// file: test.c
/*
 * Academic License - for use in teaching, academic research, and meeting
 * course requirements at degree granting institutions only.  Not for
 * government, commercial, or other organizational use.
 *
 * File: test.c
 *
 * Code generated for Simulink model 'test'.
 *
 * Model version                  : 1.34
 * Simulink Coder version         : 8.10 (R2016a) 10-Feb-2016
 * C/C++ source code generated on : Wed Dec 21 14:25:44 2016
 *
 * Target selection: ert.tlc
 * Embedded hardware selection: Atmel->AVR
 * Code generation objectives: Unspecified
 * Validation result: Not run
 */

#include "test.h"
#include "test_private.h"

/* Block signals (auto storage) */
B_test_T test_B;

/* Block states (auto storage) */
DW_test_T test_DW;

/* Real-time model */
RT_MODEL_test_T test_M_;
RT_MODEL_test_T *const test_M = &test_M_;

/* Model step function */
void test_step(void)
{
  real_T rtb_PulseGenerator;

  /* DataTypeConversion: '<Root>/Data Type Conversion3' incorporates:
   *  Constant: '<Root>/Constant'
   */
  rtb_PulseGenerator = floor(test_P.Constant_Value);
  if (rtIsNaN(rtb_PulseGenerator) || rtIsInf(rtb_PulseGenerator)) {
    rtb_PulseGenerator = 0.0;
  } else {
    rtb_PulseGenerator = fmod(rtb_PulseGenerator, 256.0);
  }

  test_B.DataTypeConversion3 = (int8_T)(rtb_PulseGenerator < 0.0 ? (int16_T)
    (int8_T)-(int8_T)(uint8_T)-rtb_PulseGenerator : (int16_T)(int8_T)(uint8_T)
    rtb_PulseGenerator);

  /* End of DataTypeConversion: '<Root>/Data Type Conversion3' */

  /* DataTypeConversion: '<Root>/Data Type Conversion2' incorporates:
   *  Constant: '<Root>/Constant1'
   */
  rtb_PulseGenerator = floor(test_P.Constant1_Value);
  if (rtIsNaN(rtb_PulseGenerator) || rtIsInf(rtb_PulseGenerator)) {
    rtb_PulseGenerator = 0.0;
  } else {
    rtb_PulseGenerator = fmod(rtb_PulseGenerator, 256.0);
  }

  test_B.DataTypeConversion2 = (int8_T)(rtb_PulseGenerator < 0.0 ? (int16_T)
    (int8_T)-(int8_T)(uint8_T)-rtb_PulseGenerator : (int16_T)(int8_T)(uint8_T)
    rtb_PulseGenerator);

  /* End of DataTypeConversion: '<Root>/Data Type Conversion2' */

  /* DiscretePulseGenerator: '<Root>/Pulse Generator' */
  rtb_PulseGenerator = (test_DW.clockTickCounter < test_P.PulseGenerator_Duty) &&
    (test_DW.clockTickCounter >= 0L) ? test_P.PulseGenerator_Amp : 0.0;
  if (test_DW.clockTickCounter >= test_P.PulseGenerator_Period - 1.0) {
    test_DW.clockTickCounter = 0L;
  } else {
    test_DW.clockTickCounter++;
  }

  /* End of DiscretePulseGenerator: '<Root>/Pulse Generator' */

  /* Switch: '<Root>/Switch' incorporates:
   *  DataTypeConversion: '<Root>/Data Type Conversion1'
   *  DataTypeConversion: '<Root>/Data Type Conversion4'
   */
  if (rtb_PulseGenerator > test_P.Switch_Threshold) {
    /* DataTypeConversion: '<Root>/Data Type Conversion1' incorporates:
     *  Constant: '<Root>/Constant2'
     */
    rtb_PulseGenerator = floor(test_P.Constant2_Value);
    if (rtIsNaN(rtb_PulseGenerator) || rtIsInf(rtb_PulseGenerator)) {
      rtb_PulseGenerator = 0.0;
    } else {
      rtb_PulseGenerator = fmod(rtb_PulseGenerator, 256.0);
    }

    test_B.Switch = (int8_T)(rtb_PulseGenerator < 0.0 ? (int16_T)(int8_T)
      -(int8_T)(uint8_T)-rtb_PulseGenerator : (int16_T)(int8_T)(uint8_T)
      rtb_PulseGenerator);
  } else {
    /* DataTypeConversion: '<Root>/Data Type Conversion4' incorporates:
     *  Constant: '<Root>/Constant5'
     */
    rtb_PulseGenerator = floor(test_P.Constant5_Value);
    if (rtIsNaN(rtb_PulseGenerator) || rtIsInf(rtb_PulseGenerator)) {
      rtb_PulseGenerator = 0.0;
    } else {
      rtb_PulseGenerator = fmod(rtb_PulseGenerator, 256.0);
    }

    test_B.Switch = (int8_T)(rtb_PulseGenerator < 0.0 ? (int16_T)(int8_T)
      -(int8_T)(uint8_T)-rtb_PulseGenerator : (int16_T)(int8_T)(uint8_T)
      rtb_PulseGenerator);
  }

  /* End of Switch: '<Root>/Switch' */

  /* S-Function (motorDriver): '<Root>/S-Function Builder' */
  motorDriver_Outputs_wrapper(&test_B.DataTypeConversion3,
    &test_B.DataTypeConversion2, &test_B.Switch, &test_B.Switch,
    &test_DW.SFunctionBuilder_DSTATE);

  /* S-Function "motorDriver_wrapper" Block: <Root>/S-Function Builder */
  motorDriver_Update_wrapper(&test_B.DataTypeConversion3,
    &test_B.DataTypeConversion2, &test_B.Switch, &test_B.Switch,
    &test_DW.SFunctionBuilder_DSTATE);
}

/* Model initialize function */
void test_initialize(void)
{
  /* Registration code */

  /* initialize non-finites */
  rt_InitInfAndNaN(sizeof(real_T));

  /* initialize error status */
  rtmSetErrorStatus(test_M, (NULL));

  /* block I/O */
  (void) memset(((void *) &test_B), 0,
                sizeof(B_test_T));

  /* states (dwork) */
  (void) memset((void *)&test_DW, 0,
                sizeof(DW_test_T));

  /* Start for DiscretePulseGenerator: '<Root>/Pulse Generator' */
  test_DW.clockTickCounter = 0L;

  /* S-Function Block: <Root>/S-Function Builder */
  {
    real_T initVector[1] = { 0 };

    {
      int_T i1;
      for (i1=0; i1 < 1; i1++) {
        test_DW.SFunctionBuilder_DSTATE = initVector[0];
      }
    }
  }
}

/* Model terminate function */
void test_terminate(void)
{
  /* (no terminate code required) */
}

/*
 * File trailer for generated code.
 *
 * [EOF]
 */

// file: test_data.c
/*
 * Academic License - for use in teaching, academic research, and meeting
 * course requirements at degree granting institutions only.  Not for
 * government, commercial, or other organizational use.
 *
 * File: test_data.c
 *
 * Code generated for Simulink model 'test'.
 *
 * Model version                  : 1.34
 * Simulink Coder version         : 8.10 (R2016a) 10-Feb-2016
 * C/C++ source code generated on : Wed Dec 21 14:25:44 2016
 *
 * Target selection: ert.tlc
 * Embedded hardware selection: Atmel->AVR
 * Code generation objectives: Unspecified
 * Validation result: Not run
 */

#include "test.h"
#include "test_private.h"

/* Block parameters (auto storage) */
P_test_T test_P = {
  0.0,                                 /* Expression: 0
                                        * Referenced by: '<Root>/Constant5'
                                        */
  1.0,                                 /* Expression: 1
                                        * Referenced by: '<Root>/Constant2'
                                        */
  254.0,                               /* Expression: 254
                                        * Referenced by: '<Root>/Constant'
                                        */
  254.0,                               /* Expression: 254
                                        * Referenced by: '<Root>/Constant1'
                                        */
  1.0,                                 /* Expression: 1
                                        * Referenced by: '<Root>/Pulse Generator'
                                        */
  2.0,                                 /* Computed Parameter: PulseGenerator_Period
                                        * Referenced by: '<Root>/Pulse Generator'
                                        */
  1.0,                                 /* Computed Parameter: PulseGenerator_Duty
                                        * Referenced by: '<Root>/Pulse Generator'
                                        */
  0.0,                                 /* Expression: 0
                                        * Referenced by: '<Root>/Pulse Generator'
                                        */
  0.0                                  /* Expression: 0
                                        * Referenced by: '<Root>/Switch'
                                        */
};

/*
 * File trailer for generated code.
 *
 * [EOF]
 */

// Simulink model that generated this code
simulink model "test"  (R2016a)
settings: Solver=FixedStepDiscrete  StartTime=0.0  StopTime=10.0  RelTol=1e-3

== system test ==
  Constant : Constant  Value=254
  Constant1 : Constant  Value=254
  Constant2 : Constant
  Constant5 : Constant  Value=0
  Data Type Conversion{1..4} (4 alike) : DataTypeConversion
  Pulse Generator : DiscretePulseGenerator  PulseType=Time based  Period=4  PulseWidth=50
  S-Function Builder : S-Function  InitFcn=try, set_param(gcb,'FunctionName','motorDriver'), end  FunctionName=motorDriver  SFunctionModules=motorDriver_wrapper  SFunctionDeploymentMode=off  EnableBusSupport=off  mask(S-Function Builder){}
      mask help: Simulink:masks:SFunctionBuilder_MD
      mask init:
      | val = [[.9  0.75 0.75 1 1 .9 .9 1]',[1 1 0.75 0.75 .9 .9 1 .9]'];try , sys = get_param(gcb,'SfunBuilderFcnName');if isempty(sys), sys = get_param(gcb,'FunctionName'); end,catch, sys = get_param(gcb,'FunctionName'); end
  Switch : Switch  Criteria=u2 > Threshold
  wires:
  Constant/1 -> Data Type Conversion3/1
  Constant1/1 -> Data Type Conversion2/1
  Constant2/1 -> Data Type Conversion1/1
  Data Type Conversion3/1 -> S-Function Builder/1
  Data Type Conversion2/1 -> S-Function Builder/2
  Data Type Conversion1/1 -> Switch/1
  Pulse Generator/1 -> Switch/2
  Data Type Conversion4/1 -> Switch/3
  Constant5/1 -> Data Type Conversion4/1
  Switch/1 -> S-Function Builder/3, S-Function Builder/4
